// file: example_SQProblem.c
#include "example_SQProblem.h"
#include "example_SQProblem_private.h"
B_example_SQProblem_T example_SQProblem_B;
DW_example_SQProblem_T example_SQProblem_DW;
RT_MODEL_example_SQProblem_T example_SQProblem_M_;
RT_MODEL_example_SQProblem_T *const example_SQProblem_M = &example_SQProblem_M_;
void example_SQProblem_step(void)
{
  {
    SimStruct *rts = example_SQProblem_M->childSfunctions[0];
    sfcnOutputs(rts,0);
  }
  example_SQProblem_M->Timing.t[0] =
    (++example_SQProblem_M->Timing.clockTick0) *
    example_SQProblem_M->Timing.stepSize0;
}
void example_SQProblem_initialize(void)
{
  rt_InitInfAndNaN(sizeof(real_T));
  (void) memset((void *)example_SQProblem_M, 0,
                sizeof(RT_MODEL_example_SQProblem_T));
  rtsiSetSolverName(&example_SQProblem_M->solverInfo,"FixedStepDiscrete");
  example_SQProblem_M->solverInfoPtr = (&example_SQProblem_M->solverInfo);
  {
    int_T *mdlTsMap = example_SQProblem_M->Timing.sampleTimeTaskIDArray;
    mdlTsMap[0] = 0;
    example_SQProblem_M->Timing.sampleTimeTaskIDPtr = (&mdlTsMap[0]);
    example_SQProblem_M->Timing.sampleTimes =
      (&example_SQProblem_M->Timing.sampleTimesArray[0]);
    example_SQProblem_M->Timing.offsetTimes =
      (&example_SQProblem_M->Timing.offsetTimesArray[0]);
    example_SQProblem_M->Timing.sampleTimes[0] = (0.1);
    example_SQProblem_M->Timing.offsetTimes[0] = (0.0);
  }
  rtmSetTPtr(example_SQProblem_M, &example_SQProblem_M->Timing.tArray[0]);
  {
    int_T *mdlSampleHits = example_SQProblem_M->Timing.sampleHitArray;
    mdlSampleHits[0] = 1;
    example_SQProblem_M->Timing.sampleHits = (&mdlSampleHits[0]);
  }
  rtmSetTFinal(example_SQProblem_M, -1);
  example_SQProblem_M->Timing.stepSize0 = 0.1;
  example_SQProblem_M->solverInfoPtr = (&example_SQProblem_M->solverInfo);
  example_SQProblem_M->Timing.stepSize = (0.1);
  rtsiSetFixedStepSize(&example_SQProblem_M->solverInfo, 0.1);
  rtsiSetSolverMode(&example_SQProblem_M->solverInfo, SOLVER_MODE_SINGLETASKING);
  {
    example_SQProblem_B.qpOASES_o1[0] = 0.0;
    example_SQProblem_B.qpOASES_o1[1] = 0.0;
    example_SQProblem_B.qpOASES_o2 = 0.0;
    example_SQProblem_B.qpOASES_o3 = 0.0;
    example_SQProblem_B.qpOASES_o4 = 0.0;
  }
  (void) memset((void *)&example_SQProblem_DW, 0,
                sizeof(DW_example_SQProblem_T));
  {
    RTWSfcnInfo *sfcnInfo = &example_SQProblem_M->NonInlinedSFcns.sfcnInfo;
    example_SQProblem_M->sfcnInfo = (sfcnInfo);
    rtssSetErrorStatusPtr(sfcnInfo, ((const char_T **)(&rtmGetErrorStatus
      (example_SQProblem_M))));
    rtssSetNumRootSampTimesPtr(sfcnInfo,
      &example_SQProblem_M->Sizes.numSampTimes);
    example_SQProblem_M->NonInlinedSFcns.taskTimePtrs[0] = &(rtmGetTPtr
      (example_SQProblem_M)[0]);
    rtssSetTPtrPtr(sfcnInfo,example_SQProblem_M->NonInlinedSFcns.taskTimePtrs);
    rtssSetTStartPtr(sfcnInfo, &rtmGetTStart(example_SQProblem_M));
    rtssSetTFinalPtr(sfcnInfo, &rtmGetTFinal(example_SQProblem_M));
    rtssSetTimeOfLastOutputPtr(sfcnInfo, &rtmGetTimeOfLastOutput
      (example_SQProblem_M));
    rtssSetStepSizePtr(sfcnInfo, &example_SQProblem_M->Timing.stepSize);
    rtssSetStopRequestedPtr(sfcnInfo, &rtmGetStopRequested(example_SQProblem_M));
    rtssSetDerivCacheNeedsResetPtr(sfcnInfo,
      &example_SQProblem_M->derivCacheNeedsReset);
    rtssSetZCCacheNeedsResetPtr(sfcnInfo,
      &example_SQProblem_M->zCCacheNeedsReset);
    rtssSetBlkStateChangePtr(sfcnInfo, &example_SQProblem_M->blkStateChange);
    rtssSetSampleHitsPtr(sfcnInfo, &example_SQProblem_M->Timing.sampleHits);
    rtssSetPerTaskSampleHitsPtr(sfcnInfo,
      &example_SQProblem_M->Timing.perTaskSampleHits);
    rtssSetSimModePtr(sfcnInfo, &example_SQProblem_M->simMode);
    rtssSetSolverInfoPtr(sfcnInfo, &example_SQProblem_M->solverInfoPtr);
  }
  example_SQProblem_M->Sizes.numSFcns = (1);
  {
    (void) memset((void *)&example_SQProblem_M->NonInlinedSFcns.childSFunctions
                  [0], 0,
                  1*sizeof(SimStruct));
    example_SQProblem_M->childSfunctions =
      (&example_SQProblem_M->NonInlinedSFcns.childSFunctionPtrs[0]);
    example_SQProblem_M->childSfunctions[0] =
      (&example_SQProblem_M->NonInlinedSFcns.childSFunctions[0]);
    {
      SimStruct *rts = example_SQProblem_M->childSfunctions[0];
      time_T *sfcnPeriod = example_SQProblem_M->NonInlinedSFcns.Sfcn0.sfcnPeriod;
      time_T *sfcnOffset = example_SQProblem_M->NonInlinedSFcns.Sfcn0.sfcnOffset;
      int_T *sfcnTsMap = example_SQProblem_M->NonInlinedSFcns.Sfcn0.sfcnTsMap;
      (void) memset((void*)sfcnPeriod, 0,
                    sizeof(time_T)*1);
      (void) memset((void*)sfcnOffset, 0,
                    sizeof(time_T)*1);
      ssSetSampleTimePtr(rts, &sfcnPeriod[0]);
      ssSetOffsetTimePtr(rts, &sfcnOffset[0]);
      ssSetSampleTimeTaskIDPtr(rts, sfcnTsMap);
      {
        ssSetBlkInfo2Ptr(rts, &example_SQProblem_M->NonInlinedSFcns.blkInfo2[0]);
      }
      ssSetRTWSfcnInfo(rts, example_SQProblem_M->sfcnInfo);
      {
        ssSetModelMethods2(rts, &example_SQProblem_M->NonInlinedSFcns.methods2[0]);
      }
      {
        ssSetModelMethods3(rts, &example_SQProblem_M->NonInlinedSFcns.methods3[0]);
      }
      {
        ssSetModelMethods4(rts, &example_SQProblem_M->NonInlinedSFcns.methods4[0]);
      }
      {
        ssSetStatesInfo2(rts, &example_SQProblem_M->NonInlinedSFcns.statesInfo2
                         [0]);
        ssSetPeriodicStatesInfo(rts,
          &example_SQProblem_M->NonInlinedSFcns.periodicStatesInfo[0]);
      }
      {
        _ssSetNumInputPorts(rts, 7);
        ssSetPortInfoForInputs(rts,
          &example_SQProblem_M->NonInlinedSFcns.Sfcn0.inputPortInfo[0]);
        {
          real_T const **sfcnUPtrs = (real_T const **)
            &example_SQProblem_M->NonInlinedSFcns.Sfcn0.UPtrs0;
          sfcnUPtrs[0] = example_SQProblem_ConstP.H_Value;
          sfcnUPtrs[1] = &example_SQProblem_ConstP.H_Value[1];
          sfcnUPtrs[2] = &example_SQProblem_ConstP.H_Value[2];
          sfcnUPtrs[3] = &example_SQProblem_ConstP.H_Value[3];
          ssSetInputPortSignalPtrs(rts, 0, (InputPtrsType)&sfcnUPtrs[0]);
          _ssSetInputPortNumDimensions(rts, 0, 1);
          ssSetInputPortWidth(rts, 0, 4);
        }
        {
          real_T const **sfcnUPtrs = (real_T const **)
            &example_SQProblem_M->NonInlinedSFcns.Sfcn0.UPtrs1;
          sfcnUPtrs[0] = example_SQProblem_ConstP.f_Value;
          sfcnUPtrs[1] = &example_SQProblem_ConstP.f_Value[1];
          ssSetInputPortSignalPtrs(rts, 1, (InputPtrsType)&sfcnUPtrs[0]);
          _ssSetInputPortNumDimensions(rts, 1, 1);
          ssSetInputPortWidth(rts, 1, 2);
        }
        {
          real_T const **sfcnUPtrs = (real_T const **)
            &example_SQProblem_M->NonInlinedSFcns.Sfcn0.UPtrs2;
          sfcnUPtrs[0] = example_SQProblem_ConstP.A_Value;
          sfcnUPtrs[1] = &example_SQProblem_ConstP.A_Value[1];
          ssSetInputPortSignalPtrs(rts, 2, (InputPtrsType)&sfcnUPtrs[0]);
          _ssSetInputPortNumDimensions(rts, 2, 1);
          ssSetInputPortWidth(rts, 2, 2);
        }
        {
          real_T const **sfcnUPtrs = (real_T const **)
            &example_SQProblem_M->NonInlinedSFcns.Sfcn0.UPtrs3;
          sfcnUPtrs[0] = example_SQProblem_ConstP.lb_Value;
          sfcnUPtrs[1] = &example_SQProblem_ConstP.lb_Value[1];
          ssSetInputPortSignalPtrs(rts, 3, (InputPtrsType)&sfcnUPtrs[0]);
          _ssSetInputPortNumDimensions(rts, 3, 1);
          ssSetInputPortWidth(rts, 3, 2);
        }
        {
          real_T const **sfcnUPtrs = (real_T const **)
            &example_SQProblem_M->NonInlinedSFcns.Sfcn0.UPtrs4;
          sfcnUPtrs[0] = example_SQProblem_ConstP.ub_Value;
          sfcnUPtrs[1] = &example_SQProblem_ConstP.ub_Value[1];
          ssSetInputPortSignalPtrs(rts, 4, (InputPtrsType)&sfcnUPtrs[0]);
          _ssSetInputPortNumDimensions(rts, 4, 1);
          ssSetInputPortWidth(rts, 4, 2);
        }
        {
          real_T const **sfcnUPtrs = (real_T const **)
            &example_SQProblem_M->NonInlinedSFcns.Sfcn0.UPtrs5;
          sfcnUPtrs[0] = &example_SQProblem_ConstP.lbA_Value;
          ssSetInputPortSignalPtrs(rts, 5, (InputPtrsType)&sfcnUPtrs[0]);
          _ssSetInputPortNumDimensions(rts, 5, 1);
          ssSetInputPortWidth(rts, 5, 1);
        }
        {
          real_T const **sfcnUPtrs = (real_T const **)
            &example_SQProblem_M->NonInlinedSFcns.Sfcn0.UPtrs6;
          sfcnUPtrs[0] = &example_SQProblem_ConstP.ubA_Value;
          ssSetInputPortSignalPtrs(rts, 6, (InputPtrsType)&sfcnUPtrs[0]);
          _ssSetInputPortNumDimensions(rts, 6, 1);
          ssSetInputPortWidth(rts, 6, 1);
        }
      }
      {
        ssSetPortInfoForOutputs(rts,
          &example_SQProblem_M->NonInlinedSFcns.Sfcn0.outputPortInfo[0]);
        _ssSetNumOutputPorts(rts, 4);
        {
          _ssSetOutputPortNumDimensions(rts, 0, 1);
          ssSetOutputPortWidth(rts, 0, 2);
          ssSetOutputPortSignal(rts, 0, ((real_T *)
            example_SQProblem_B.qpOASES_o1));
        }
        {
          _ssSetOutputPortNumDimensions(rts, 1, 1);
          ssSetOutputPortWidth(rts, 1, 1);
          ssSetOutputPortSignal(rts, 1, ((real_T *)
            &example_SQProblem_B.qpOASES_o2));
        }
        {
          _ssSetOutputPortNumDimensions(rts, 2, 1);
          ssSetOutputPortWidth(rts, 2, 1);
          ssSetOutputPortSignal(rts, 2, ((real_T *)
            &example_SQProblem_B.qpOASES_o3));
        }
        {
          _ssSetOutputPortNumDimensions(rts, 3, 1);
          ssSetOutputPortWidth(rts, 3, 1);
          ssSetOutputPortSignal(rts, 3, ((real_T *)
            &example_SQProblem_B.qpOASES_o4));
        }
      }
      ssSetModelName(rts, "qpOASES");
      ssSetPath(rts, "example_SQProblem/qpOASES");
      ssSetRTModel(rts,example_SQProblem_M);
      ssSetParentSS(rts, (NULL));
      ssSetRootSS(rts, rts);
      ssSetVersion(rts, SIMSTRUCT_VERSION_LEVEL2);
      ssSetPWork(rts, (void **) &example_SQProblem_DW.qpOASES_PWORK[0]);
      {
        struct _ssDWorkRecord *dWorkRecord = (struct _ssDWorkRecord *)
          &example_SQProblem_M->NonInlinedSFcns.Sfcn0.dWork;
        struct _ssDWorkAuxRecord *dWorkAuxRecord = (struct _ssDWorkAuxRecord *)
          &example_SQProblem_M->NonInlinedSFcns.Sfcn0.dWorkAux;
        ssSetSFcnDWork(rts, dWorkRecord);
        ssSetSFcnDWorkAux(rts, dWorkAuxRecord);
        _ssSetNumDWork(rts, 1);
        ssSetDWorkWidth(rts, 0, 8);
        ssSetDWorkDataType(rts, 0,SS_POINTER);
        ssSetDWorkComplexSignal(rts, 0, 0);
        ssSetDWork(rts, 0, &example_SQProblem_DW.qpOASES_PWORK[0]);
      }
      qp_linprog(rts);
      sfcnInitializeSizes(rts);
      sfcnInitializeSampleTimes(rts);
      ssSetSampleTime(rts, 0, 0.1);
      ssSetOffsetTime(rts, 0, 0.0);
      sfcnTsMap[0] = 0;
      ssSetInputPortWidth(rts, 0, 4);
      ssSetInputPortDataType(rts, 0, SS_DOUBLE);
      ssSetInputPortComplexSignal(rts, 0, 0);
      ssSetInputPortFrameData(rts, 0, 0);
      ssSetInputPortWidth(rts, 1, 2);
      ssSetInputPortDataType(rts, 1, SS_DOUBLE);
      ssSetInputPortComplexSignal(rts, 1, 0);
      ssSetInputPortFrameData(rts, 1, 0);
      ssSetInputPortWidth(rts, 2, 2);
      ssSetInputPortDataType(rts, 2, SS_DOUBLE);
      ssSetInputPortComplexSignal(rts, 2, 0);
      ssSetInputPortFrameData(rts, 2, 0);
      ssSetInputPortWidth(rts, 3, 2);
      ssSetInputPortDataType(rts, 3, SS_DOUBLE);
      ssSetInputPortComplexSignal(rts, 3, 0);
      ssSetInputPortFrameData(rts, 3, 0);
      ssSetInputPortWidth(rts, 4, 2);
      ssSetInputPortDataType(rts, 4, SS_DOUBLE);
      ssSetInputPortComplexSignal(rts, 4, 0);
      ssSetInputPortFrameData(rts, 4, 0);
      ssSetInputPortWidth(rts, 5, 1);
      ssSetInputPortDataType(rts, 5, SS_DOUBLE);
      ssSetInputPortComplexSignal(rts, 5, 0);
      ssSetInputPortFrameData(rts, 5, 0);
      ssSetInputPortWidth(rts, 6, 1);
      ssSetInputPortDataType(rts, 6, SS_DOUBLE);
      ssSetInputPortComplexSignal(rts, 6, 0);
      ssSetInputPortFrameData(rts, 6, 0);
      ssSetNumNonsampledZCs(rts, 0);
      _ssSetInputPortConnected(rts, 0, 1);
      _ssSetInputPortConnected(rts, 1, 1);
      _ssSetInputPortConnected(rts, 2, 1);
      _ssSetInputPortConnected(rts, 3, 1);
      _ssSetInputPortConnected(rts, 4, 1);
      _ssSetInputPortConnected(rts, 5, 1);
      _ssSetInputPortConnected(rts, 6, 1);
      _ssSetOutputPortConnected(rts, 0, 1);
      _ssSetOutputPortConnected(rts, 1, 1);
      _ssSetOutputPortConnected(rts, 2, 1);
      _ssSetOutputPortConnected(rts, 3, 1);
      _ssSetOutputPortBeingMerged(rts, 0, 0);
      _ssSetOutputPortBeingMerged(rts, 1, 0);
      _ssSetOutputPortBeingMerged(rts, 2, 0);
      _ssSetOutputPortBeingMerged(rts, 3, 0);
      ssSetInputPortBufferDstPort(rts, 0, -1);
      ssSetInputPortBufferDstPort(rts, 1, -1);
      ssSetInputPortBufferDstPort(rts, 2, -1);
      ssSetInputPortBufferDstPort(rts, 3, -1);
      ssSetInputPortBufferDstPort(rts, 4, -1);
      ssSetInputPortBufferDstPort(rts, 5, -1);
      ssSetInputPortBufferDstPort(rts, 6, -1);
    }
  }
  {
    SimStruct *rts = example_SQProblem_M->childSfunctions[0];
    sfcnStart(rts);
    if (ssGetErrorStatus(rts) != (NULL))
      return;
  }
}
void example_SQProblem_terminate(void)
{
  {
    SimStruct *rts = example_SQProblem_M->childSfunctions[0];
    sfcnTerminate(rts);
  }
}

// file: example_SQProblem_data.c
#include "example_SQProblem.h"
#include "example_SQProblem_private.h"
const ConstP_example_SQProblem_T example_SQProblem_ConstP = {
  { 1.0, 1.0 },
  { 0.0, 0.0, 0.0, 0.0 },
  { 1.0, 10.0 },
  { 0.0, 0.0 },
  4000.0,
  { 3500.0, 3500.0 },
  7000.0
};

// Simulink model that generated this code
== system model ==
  qpOASES : S-Function  FunctionName=qp_linprog  <- 1: Constant#1, 2: Constant#2, 3: Constant#3, 4: lb, 5: ub, 6: lbA, 7: ubA
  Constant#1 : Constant  Value=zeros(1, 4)
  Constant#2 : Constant  Value=[1 10]
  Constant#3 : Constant  Value=[1 1]
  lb : Constant  Value=[0 0]
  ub : Constant  Value=[3500 3500]
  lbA : Constant  Value=[4000]
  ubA : Constant  Value=[7000]
